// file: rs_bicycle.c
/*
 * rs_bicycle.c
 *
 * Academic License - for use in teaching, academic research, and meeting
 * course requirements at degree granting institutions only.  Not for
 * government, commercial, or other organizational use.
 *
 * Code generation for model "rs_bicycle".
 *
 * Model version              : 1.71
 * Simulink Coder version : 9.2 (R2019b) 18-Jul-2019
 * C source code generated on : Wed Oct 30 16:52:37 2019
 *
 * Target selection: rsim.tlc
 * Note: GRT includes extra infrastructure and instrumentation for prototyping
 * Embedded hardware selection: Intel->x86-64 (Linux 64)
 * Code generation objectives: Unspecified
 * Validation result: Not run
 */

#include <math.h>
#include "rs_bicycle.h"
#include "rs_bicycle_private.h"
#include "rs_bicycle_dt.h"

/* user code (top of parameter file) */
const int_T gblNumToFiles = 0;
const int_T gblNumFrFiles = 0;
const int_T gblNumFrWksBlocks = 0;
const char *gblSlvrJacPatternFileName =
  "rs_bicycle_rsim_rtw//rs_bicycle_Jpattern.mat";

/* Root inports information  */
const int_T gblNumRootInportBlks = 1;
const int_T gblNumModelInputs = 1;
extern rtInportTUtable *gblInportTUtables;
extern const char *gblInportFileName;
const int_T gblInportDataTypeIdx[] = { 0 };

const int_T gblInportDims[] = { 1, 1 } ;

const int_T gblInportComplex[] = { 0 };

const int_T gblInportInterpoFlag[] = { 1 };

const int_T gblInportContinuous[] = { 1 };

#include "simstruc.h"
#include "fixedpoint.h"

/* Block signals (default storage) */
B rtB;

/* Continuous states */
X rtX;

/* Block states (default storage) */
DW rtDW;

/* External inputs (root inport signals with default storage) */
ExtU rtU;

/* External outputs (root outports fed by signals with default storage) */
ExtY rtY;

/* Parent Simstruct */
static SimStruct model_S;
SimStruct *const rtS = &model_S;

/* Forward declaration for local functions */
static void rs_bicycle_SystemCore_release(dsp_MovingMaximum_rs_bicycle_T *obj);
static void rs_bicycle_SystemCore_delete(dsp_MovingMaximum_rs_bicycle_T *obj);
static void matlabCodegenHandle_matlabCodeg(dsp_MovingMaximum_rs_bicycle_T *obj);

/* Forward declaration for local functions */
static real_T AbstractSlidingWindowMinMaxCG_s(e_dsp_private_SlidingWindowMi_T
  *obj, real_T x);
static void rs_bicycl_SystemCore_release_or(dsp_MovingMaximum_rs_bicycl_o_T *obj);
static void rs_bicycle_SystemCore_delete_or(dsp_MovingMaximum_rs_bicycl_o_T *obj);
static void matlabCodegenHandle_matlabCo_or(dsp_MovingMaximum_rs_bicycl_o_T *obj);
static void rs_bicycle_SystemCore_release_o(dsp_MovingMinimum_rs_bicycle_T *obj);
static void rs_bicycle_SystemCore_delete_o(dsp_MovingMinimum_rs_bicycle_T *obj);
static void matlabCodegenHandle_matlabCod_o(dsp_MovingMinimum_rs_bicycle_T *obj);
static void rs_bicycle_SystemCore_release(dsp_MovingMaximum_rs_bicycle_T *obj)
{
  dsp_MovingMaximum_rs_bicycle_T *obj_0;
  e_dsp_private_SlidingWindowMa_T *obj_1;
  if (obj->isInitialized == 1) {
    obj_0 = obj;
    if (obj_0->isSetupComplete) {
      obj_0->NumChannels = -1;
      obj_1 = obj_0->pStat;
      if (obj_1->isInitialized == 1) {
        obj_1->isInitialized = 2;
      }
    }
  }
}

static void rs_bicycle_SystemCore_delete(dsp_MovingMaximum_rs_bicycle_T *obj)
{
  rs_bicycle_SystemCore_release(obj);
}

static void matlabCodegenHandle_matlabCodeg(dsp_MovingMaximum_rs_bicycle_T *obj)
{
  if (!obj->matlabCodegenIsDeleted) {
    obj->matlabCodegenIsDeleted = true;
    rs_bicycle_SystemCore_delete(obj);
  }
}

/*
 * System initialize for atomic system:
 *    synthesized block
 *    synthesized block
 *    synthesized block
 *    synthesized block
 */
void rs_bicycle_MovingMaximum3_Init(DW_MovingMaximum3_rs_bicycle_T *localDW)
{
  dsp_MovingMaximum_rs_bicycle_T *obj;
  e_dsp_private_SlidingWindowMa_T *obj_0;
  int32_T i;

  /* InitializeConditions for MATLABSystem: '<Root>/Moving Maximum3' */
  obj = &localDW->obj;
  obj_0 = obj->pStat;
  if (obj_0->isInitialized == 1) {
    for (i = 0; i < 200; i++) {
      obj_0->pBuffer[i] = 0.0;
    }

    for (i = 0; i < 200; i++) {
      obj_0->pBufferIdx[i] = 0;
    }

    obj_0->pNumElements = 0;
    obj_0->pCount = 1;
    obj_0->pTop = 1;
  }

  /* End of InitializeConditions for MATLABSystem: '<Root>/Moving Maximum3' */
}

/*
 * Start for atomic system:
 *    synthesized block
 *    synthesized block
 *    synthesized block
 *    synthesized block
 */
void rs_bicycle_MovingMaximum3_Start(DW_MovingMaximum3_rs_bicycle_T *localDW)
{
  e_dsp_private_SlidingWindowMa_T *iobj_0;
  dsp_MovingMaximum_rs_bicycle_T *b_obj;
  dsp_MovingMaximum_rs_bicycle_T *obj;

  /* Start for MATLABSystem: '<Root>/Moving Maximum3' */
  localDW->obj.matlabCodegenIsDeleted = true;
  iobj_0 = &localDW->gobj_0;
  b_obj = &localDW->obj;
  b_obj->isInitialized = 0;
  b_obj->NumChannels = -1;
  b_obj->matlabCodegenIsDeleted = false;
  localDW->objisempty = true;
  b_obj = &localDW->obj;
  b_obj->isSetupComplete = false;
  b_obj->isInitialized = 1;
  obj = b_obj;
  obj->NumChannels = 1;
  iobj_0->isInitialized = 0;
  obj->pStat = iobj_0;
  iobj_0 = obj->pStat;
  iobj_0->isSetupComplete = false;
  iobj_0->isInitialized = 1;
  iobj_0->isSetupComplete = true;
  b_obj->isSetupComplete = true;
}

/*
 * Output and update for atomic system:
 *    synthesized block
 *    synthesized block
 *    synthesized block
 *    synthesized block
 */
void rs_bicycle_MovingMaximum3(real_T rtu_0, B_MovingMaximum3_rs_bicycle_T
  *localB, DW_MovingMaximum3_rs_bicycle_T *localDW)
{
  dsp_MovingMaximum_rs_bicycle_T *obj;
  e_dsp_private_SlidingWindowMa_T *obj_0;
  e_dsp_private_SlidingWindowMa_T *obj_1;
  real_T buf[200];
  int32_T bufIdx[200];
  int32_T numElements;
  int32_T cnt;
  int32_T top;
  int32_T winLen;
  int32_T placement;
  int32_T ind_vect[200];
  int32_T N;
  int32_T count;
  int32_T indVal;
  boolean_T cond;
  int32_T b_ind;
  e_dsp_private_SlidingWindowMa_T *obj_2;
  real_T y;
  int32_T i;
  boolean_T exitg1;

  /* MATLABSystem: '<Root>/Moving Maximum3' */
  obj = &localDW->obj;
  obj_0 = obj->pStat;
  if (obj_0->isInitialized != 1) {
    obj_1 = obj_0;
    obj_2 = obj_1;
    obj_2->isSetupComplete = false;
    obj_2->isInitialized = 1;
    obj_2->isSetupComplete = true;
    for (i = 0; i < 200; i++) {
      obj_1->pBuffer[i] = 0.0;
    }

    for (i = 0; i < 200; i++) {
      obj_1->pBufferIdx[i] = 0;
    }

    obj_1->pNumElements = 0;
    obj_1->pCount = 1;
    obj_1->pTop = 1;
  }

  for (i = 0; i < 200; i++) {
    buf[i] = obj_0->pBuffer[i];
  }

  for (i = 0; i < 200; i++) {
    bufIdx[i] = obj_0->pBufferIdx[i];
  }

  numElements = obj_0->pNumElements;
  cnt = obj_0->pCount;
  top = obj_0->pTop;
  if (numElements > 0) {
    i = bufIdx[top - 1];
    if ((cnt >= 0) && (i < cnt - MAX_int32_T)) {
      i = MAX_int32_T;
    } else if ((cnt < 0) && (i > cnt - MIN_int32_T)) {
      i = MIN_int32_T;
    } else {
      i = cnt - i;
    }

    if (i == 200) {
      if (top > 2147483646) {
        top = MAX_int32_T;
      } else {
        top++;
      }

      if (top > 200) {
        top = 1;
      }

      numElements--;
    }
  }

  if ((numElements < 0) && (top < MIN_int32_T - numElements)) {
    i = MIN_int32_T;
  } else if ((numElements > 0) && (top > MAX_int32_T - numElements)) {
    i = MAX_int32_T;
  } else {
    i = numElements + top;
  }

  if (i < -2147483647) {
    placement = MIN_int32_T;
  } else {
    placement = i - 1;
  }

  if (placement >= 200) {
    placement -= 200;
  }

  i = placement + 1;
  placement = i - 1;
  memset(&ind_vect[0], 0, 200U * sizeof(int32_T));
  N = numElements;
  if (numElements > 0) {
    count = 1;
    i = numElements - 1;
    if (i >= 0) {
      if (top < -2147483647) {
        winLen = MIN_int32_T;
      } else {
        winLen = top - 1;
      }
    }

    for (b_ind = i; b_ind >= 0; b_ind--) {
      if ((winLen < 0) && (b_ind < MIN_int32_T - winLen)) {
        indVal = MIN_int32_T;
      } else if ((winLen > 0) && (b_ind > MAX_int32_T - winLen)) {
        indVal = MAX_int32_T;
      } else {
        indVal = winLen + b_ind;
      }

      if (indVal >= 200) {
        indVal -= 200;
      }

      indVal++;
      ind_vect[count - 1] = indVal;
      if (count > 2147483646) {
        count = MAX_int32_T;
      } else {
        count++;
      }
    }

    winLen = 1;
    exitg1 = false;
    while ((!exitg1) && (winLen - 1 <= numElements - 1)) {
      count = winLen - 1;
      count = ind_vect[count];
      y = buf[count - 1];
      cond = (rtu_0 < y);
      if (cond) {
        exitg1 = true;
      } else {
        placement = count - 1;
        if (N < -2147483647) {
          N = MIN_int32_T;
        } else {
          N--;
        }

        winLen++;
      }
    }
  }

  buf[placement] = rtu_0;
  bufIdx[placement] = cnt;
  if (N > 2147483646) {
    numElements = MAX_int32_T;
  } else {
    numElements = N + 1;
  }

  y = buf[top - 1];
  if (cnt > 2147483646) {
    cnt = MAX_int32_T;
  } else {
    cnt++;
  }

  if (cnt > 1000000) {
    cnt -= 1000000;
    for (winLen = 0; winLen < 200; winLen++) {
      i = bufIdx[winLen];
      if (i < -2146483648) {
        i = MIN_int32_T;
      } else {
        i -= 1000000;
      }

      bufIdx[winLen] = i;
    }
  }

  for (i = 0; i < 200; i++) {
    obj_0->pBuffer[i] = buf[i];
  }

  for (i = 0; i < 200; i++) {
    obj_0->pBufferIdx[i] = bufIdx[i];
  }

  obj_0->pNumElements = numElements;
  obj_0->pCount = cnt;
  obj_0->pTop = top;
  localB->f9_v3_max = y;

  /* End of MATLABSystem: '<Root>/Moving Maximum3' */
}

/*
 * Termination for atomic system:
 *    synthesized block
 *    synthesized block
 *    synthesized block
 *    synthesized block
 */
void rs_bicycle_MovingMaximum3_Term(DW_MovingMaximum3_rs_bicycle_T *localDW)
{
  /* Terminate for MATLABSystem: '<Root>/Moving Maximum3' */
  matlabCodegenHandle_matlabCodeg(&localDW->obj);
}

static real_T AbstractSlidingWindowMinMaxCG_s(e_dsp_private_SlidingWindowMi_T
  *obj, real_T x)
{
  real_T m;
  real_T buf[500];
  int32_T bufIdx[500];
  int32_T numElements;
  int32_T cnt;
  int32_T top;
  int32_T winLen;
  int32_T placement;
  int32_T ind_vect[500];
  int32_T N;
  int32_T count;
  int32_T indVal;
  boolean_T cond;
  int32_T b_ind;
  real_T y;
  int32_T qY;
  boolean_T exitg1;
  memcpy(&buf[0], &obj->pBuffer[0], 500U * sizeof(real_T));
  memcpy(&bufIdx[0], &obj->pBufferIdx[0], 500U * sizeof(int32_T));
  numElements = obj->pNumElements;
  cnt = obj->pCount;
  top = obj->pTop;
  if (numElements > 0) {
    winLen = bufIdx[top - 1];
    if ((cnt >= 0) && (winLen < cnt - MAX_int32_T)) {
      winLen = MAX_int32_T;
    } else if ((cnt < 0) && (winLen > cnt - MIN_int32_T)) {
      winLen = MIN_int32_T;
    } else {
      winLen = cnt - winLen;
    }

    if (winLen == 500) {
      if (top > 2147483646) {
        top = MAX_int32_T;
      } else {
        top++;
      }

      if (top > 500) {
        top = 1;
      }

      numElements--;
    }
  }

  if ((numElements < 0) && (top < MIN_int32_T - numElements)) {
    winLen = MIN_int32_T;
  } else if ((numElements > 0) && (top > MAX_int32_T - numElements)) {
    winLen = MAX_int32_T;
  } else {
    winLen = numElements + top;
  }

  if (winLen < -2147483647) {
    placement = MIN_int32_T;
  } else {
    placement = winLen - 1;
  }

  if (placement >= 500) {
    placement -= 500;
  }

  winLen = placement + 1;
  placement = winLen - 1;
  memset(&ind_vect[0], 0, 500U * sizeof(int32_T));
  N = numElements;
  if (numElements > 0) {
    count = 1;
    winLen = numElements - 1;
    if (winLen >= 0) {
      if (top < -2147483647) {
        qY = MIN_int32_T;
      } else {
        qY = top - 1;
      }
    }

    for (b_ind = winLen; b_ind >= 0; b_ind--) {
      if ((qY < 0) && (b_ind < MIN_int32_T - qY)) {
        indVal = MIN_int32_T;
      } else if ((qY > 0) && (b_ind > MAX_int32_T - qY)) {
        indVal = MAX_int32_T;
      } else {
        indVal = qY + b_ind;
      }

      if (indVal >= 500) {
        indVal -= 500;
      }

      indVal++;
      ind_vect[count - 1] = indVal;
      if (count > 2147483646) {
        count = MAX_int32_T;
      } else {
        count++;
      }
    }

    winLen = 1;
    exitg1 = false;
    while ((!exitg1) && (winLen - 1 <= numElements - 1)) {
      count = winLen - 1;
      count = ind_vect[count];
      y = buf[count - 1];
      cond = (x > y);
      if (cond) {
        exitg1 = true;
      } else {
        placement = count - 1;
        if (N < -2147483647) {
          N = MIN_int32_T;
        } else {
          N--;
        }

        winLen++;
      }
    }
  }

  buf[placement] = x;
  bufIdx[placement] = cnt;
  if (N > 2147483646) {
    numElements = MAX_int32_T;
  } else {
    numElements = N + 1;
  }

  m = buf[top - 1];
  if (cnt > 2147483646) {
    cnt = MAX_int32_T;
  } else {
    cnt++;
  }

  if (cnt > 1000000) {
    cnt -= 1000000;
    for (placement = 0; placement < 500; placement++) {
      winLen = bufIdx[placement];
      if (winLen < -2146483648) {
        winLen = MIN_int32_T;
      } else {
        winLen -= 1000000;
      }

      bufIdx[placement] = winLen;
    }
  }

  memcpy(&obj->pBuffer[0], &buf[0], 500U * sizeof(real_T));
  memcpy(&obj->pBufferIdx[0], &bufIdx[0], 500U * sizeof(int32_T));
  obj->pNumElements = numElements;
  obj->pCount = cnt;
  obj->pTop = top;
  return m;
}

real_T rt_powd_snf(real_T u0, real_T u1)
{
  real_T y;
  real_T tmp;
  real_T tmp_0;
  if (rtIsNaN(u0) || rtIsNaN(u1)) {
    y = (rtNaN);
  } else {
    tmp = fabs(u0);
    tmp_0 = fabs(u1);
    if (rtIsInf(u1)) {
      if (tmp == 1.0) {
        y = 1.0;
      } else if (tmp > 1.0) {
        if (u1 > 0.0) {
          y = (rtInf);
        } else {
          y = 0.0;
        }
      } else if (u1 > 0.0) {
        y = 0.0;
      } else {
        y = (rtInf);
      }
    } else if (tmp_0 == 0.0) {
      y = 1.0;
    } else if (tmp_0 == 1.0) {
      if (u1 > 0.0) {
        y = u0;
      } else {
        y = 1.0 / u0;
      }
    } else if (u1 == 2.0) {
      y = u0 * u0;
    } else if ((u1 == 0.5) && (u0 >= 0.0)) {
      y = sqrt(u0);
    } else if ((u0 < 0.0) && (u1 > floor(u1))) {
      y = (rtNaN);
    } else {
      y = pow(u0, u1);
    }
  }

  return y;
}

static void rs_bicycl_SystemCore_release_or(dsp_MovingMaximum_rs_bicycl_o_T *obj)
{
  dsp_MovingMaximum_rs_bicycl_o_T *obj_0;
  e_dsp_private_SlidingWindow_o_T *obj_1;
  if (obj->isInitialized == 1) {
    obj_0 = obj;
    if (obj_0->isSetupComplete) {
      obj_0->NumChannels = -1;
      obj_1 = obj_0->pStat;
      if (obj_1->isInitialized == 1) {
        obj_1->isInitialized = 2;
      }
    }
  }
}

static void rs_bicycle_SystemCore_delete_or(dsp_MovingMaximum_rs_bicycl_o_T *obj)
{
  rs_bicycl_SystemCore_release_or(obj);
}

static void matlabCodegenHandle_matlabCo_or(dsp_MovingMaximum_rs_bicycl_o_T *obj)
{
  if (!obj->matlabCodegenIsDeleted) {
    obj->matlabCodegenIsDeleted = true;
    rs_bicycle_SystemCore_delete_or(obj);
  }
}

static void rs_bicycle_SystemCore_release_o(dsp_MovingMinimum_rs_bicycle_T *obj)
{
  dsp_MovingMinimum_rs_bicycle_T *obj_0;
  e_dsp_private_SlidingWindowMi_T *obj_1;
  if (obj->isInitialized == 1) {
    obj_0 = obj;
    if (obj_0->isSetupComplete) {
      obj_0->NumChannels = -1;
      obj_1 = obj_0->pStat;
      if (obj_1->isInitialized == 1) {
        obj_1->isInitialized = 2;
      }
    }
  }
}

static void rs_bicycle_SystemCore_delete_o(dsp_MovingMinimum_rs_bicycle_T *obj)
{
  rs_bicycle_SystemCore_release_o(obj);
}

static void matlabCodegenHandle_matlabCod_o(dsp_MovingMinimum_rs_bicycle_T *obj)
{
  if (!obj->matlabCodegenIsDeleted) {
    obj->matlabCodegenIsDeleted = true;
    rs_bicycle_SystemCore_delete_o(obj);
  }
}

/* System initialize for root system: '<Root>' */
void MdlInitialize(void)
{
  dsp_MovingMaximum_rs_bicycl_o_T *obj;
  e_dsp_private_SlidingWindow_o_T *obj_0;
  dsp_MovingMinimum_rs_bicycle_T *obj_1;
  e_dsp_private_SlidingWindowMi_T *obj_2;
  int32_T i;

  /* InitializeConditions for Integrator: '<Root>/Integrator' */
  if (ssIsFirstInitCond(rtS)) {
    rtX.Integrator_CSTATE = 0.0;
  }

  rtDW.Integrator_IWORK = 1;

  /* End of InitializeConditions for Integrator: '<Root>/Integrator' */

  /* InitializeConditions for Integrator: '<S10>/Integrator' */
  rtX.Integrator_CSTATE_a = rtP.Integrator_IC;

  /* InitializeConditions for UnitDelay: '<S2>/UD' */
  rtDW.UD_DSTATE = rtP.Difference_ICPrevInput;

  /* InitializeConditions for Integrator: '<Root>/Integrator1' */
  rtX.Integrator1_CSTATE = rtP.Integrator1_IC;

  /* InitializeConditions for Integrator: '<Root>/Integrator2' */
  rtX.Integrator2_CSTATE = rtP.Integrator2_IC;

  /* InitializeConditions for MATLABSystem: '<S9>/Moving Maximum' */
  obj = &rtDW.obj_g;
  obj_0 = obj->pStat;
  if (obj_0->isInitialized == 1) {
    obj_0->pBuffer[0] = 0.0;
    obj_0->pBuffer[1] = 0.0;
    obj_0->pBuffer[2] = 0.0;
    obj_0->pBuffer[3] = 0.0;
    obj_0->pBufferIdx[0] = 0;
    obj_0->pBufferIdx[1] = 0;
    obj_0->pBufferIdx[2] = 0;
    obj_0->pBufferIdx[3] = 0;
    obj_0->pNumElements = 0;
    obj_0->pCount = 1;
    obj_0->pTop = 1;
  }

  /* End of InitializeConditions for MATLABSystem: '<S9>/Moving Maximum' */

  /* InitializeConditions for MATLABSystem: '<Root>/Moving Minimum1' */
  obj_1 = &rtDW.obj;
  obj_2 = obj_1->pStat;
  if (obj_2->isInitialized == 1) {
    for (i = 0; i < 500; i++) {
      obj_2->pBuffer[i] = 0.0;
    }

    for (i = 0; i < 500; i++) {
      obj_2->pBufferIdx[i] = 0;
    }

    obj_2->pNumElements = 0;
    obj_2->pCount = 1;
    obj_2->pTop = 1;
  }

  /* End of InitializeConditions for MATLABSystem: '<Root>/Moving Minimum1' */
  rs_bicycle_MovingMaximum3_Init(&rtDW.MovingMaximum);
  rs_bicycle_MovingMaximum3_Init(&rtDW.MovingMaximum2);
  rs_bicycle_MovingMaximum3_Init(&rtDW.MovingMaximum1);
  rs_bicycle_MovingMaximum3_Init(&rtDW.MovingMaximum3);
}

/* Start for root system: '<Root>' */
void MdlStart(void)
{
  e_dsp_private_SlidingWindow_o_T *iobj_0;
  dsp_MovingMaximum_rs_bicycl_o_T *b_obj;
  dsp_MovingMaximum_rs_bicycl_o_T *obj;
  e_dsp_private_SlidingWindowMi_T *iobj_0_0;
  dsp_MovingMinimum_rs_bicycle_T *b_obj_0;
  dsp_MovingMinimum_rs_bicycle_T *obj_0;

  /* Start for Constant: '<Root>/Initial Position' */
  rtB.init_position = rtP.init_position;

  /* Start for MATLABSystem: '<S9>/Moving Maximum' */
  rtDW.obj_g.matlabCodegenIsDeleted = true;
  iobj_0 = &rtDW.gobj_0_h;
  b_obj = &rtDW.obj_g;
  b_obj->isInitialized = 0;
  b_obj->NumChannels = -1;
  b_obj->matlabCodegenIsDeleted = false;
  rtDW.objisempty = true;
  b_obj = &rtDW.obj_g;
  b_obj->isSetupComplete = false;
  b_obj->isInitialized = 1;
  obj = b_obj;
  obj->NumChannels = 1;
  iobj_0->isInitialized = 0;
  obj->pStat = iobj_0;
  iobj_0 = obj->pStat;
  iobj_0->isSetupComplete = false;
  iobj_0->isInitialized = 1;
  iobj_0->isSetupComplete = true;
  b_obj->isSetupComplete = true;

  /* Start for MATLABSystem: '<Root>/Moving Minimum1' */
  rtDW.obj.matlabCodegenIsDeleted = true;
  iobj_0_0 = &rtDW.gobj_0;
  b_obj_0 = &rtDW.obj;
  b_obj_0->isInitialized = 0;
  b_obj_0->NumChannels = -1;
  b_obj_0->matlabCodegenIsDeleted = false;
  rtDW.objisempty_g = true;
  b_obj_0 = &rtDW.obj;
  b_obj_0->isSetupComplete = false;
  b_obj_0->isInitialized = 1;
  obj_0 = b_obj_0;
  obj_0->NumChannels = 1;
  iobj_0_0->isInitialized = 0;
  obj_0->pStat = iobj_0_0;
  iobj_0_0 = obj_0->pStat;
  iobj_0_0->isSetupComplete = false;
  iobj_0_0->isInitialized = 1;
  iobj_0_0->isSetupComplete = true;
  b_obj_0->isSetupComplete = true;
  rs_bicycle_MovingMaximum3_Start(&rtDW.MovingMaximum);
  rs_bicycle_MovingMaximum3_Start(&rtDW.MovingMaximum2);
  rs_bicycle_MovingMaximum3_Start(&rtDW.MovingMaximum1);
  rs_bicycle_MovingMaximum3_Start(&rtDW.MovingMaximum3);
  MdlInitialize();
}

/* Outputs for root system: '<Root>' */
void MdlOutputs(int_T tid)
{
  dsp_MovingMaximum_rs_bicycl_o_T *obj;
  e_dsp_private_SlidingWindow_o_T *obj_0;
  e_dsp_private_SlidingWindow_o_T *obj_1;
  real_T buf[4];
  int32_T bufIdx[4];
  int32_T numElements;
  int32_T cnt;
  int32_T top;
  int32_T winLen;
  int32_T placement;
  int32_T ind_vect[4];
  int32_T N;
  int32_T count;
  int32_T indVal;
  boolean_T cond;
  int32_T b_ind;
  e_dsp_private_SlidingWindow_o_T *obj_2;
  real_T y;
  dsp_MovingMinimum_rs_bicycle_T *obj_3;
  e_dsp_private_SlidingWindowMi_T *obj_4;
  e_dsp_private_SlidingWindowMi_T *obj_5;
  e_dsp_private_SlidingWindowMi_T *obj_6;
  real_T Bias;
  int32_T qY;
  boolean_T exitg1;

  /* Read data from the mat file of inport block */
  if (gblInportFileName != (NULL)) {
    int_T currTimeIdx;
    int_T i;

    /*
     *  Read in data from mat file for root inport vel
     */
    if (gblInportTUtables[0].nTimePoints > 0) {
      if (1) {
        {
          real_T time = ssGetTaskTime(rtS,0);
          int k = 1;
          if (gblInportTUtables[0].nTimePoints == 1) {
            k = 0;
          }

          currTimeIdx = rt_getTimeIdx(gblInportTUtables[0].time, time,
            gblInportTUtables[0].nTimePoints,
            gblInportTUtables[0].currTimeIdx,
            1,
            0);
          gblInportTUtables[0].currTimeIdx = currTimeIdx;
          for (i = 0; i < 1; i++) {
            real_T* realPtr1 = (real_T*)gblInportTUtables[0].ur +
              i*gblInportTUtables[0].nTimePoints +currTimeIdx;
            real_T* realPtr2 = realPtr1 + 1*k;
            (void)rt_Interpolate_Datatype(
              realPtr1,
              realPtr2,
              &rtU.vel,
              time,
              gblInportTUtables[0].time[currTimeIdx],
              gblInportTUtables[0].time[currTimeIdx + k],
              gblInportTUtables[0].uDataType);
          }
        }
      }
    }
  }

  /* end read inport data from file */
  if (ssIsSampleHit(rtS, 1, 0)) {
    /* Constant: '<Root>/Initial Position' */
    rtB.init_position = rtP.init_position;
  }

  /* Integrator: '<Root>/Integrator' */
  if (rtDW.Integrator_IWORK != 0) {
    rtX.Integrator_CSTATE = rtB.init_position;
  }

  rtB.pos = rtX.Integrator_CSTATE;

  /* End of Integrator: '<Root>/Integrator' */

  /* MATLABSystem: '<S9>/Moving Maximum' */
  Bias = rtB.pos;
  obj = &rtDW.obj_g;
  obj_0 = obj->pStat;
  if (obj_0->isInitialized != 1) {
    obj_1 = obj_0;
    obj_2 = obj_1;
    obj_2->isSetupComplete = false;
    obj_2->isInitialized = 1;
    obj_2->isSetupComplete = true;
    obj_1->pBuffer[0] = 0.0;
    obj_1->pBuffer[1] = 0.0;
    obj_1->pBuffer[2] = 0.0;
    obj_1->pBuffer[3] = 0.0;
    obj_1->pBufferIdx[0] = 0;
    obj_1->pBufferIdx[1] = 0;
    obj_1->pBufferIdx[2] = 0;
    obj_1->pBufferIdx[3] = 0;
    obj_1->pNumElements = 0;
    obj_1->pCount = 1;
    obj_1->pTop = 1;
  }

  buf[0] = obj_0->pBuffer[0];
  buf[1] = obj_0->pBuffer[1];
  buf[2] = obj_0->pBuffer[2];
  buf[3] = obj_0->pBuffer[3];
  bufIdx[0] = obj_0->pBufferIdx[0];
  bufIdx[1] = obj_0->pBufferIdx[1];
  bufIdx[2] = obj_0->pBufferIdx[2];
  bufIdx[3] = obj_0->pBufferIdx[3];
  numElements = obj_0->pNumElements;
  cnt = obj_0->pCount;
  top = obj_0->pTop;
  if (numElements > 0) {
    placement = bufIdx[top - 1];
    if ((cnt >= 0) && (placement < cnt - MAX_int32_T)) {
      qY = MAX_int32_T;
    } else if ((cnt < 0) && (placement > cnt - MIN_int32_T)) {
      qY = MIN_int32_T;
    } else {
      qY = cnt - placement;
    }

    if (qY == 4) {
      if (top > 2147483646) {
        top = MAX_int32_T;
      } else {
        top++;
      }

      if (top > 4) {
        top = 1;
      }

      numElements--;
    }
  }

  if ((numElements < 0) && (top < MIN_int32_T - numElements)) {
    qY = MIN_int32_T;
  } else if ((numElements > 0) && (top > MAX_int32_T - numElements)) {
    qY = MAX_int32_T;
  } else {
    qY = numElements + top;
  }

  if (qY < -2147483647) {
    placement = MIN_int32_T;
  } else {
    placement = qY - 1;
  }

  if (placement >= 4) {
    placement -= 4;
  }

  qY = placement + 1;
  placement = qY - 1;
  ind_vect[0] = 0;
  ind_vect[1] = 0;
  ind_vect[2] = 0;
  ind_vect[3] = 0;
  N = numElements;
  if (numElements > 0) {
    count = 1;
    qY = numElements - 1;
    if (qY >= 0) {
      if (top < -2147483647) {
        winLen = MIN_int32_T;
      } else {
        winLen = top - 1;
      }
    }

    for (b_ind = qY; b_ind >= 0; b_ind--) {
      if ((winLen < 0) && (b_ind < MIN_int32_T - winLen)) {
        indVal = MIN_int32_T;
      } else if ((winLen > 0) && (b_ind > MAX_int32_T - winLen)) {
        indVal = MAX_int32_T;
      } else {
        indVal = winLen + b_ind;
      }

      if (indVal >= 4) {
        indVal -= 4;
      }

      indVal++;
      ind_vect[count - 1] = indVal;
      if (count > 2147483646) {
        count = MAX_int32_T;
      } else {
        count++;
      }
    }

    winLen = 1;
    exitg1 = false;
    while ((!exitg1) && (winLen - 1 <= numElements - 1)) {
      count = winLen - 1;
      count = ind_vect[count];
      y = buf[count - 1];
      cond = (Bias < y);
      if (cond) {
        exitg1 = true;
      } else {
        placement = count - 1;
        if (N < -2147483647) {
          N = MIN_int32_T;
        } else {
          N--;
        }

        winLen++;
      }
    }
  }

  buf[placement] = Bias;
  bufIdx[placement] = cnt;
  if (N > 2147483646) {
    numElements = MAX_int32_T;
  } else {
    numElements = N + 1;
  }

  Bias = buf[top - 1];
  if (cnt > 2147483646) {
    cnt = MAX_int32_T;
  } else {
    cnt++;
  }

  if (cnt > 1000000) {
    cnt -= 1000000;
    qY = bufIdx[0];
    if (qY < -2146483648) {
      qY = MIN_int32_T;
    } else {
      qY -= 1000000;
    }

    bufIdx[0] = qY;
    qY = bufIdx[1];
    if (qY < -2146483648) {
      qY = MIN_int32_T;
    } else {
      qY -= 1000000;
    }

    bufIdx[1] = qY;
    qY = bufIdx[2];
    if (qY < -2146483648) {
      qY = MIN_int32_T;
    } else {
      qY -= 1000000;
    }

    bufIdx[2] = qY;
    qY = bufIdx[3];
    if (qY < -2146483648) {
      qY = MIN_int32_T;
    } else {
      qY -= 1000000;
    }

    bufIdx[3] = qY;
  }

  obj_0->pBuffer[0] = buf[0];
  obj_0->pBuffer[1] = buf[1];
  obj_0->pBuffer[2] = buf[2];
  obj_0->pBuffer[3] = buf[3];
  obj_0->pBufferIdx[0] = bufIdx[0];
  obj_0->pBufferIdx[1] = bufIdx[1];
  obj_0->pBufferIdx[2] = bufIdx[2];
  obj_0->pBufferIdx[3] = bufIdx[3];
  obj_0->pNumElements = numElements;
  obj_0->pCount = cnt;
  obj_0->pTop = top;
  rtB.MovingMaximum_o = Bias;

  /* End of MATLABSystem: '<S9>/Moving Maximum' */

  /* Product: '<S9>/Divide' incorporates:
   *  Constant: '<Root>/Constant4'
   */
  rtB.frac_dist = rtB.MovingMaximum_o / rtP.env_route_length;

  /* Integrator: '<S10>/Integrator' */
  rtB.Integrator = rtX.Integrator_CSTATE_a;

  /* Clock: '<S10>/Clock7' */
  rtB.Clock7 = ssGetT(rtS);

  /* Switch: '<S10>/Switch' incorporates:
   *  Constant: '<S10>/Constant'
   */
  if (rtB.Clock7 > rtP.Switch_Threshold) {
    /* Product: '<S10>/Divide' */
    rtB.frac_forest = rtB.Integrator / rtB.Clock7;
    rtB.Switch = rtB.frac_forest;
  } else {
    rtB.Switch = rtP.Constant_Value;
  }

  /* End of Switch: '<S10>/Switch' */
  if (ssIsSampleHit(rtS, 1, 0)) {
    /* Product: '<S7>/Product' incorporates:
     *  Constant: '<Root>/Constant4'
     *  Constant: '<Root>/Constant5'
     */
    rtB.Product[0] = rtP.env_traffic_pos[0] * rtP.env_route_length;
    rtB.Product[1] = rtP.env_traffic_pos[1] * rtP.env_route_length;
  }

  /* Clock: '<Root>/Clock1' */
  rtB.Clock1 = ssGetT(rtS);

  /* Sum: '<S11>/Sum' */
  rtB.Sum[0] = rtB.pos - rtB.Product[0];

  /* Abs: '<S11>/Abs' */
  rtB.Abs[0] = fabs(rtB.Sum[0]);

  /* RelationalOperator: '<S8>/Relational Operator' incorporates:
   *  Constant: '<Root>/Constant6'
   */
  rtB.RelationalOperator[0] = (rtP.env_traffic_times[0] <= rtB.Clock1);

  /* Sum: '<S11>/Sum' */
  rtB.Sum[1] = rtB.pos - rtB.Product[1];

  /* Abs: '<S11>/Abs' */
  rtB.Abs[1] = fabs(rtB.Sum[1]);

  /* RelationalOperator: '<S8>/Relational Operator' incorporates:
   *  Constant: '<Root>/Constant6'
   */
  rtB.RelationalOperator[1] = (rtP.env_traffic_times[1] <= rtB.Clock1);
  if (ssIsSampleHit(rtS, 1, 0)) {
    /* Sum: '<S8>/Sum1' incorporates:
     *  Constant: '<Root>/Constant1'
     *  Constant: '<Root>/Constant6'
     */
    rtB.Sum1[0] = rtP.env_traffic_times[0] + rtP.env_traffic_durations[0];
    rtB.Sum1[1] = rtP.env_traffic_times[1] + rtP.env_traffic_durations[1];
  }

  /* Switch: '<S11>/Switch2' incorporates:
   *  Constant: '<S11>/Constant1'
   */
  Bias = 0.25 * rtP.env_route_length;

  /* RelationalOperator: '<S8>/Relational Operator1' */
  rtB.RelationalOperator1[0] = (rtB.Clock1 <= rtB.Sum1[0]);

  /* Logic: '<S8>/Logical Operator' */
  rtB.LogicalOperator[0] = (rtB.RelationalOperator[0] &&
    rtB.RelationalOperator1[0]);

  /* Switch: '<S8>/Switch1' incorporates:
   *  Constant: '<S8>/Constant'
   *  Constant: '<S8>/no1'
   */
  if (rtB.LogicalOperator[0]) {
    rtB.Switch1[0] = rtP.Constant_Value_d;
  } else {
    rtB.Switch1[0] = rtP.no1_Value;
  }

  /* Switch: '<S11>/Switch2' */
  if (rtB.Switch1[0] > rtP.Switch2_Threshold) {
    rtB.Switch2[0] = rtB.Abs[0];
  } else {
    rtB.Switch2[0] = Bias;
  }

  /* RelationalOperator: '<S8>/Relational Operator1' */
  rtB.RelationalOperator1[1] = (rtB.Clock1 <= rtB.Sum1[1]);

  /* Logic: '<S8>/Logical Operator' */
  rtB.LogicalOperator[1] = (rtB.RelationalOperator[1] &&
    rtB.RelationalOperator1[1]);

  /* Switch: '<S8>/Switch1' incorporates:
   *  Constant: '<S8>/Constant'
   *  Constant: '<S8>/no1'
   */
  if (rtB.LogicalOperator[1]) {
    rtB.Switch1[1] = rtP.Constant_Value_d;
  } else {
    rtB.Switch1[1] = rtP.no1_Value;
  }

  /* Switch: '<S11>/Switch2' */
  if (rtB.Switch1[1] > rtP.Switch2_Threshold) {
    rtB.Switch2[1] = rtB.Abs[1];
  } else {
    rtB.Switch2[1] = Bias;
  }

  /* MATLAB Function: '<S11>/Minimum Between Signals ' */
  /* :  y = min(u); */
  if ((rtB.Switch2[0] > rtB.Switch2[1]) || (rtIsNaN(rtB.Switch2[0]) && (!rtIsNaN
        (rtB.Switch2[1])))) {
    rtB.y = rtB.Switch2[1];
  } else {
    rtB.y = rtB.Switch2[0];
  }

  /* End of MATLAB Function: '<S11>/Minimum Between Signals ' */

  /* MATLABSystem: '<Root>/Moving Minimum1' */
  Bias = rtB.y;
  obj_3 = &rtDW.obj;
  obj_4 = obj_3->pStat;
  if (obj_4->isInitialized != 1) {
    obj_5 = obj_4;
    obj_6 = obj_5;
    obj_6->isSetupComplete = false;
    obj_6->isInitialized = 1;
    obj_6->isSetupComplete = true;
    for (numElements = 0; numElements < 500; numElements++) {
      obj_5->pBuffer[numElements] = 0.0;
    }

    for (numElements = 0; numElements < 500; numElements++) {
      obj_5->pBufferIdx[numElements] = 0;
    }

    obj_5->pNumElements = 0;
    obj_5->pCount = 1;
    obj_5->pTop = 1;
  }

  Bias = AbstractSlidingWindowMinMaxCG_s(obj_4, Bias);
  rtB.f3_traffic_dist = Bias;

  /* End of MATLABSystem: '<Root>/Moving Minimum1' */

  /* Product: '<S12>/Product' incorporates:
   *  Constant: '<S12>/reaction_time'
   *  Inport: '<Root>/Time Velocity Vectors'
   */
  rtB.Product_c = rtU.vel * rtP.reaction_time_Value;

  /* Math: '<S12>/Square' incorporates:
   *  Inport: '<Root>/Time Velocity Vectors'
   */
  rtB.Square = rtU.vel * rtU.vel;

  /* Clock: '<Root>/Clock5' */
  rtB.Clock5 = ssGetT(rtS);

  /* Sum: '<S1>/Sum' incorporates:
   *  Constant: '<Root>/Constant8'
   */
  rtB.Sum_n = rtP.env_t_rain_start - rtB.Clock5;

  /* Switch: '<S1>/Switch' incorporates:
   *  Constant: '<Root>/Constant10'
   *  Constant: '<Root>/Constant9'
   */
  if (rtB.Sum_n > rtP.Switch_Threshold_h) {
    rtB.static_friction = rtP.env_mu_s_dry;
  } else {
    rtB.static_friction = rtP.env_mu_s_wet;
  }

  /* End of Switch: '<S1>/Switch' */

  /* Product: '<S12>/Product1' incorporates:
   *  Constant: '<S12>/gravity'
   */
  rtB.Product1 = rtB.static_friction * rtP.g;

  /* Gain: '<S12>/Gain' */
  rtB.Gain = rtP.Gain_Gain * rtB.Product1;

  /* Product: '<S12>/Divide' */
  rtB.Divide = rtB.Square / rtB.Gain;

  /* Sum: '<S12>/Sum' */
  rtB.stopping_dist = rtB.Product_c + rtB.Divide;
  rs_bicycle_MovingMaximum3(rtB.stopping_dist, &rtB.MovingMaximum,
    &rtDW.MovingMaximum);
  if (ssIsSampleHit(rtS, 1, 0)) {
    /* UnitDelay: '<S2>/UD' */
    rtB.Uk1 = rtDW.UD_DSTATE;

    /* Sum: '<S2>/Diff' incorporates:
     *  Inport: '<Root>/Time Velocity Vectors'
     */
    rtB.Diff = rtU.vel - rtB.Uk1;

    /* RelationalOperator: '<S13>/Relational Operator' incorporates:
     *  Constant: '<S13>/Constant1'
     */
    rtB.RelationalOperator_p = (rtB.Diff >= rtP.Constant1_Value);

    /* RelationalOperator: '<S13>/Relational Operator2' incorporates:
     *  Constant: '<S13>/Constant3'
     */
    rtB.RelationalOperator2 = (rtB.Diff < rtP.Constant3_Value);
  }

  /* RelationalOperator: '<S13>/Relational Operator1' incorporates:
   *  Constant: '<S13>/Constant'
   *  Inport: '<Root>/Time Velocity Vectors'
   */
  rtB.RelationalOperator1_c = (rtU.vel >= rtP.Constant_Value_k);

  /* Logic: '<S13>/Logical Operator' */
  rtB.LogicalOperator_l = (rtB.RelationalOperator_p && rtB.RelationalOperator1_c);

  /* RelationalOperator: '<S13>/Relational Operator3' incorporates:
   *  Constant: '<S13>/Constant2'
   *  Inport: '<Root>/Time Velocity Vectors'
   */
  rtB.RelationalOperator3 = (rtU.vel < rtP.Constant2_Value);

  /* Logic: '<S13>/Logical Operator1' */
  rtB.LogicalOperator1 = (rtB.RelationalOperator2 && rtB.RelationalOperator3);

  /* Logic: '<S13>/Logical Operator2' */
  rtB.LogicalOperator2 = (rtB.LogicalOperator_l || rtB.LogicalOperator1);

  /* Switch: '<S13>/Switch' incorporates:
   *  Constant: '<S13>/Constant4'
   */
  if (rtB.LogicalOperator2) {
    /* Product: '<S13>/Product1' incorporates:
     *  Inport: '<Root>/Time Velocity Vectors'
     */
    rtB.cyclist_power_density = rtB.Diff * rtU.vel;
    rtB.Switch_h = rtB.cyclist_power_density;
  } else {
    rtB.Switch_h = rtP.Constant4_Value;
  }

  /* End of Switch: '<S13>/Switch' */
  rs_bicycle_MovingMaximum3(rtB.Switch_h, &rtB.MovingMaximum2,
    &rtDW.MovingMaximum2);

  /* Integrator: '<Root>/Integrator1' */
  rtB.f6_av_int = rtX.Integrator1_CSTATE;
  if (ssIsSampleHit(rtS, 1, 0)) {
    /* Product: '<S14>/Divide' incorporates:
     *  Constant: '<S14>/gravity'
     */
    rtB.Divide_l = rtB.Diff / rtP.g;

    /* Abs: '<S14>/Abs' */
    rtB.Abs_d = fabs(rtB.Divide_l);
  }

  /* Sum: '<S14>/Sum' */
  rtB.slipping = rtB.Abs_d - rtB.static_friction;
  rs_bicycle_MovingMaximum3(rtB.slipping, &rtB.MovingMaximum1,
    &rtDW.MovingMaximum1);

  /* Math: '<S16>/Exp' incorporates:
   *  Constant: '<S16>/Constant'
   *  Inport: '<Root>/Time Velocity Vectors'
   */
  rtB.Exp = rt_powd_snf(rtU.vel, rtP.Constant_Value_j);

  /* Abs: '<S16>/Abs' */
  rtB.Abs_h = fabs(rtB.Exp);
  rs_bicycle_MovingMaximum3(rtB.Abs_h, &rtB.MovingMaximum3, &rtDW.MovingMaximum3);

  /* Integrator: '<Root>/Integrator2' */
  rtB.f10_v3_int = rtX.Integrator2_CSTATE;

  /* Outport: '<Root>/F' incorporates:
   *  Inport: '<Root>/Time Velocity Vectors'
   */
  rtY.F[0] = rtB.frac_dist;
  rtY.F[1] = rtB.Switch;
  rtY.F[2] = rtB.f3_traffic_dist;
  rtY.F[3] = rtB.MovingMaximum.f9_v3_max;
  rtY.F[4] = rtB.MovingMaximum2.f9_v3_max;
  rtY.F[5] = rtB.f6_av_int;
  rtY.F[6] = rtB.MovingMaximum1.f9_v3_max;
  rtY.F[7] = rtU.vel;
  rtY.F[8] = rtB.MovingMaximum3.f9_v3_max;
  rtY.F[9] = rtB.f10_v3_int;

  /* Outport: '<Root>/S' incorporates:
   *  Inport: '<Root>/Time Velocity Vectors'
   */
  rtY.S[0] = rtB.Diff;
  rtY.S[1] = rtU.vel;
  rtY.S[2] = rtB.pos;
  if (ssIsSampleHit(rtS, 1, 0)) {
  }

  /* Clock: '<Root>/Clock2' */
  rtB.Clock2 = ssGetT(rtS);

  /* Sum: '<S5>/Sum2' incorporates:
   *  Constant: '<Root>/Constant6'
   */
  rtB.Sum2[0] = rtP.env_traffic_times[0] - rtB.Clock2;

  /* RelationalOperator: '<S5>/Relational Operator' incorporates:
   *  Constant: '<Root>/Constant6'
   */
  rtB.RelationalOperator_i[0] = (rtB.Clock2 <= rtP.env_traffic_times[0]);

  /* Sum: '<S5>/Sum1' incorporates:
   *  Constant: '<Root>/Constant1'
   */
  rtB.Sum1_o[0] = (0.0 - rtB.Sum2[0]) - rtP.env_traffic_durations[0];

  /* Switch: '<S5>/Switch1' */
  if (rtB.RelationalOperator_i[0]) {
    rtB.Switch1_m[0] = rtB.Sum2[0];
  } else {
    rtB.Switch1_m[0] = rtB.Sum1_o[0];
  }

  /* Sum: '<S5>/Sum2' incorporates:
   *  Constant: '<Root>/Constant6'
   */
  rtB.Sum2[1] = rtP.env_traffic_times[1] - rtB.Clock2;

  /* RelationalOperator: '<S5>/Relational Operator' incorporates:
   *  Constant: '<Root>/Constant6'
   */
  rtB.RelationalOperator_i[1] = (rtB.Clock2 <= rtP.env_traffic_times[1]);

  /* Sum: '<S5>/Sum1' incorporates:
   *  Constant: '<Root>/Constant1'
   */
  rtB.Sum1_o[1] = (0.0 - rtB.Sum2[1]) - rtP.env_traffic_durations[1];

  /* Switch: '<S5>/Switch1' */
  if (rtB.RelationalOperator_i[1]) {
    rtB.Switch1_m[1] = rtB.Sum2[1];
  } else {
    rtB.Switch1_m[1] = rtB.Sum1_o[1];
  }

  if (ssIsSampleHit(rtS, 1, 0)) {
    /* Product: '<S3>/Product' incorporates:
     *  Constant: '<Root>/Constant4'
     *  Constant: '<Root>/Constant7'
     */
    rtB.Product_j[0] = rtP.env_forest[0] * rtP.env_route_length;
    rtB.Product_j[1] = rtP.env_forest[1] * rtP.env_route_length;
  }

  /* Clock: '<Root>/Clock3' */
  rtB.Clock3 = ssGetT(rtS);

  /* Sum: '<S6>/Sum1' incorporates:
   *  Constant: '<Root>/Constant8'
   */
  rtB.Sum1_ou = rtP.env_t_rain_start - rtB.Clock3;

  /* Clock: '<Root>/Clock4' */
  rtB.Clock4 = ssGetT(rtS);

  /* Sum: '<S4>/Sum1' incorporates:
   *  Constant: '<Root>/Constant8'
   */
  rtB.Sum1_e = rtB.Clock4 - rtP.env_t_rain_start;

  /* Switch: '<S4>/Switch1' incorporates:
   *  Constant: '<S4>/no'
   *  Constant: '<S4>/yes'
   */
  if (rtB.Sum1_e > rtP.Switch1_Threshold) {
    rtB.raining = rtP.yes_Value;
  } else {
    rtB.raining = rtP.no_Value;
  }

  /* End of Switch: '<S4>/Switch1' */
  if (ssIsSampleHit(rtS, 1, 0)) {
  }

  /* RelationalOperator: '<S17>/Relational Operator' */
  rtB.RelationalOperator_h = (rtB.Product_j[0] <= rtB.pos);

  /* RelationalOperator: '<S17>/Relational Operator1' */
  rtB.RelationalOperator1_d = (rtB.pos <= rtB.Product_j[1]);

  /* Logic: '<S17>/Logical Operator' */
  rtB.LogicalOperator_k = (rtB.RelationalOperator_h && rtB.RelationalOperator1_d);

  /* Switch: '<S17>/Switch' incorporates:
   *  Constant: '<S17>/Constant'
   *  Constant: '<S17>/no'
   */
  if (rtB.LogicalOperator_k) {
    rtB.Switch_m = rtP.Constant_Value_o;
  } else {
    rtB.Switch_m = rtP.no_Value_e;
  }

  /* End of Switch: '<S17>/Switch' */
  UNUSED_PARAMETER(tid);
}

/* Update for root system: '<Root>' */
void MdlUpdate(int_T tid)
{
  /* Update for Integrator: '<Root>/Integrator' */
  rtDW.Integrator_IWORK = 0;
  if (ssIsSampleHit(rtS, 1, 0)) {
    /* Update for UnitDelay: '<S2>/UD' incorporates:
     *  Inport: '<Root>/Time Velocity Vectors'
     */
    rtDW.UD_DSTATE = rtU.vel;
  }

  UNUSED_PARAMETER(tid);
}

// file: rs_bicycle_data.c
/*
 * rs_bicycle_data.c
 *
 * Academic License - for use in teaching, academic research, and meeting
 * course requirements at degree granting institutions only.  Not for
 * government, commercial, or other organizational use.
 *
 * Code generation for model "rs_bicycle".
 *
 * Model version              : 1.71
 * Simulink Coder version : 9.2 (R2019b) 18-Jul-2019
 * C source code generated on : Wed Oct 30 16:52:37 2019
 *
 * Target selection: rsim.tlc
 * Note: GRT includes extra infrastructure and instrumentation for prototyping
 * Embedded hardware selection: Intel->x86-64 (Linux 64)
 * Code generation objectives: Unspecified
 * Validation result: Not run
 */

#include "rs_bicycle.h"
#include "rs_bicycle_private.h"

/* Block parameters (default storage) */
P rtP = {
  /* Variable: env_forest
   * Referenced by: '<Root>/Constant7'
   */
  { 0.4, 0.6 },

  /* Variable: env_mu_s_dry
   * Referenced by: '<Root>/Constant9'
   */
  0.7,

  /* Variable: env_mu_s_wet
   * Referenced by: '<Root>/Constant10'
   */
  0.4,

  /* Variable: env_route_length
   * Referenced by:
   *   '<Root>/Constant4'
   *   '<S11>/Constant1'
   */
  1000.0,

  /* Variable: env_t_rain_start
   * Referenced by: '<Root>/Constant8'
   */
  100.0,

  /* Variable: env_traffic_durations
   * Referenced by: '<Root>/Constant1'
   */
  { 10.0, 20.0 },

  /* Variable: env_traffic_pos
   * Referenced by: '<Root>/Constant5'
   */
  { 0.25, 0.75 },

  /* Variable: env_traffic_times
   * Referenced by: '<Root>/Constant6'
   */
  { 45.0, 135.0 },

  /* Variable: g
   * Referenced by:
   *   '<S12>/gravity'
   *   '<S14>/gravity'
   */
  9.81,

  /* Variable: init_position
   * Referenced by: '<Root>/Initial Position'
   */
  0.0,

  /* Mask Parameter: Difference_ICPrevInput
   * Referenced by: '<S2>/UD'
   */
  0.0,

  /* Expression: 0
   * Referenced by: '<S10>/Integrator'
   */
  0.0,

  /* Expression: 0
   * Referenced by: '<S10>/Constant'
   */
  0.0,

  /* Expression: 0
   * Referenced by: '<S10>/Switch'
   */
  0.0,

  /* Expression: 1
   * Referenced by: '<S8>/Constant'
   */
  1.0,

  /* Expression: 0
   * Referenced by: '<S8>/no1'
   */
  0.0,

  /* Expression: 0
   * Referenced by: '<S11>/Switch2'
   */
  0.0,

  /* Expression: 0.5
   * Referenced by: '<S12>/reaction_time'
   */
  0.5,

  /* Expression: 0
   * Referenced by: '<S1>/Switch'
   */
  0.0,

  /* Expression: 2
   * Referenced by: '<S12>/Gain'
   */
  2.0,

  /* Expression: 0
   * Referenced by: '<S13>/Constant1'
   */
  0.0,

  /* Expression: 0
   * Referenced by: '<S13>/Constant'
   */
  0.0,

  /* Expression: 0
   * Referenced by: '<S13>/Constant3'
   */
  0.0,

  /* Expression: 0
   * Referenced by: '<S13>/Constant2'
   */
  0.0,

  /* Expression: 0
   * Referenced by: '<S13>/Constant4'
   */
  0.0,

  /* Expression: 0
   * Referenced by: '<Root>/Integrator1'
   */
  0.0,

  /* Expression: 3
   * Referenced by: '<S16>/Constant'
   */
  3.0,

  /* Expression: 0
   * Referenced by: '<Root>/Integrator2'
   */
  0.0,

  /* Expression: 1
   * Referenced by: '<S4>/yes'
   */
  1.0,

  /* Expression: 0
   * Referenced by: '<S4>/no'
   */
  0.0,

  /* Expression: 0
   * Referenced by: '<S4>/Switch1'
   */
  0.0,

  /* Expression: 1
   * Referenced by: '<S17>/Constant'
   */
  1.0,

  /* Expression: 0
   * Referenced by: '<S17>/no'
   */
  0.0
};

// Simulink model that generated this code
simulink model "rs_bicycle"  (R2019b)
settings: Solver=FixedStepAuto  StartTime=0.0  StopTime=200  FixedStep=4  RelTol=1e-3
undefined symbols (not defined in the file): duration, env_forest, env_mu_s_dry, env_mu_s_wet, env_route_length, env_t_rain_start, env_traffic_durations, env_traffic_pos, env_traffic_times, g, init_position
libraries: dspstat3 x6, simulink x1

== system rs_bicycle ==
  note: Guidance Solution for
      | Dynamics $\mathcal{S}(t)$
  note: Fixed Decision
      | Components $(s)$
  note: Environment Parameters $\mathcal{P}(t)$
  note: 'From Velocity'
      | Constructor $\mathcal{C}(x,p)$
  note: Transient Parameter Limit $\mathcal{P}(t)$
  Time Velocity Vectors : Inport
  Auxilliary Scope : Scope  NumInputPorts=6
  Bus Creator : BusCreator  Inputs=2
  Bus Creator1 : BusCreator  Inputs=9
  Bus Creator2 : BusCreator  Inputs=3
  Bus Creator3 : BusCreator  Inputs=4
  Bus Creator4 : BusCreator  Inputs=7
  Bus Creator5 : BusCreator  Inputs=10
  Clock{1..5} (5 alike) : Clock
  Constant1 : Constant  Value=env_traffic_durations
  Constant10 : Constant  Value=env_mu_s_wet
  Constant4 : Constant  Value=env_route_length
  Constant5 : Constant  Value=env_traffic_pos
  Constant6 : Constant  Value=env_traffic_times
  Constant7 : Constant  Value=env_forest
  Constant8 : Constant  Value=env_t_rain_start
  Constant9 : Constant  Value=env_mu_s_dry
  Current Static Friction : Subsystem
  Difference : simulink/Discrete/Difference  ICPrevInput=0.0  OutMin=[]  OutMax=[]  OutDataType=fixdt(1, 16)  OutScaling=2^-10  RndMeth=Round  DoSatur=off
  Duration : Constant  Value=duration
  Forest Boundaries : Subsystem
  Initial Position : Constant  Value=init_position
  Integrator : Integrator  InitialConditionSource=external  InitialCondition=init_position
  Integrator1 : Integrator
  Integrator2 : Integrator
  Moving Maximum{,1..3} (4 alike) : dspstat3/Moving Maximum  SpecifyWindowLength=on  WindowLength=duration  SimulateUsing=Code generation
  Moving Minimum1 : dspstat3/Moving Minimum  SpecifyWindowLength=on  WindowLength=500  SimulateUsing=Code generation
  Performance Metric Scope : Scope  NumInputPorts=10
  Raining Boolean : Subsystem
  Scope2 : Scope  NumInputPorts=7
  Solution Scope : Scope  NumInputPorts=3
  Time From Traffic Encounter : Subsystem
  Time Until Raining : Subsystem
  To Workspace : ToWorkspace  VariableName=WS_S  SaveFormat=Timeseries  SampleTime=-1
  To Workspace1 : ToWorkspace  VariableName=WS_s  SaveFormat=Timeseries  SampleTime=-1
  To Workspace2 : ToWorkspace  VariableName=WS_P  SaveFormat=Timeseries  SampleTime=-1
  To Workspace3 : ToWorkspace  VariableName=WS_p  SaveFormat=Timeseries  SampleTime=-1
  To Workspace4 : ToWorkspace  VariableName=wf  SaveFormat=Timeseries  SampleTime=-1
  Traffic Location(s) : Subsystem
  Traffic Passing : Subsystem
  aux1: Fraction of Route Distance : Subsystem
  aux2: Fraction Spent In Forest : Subsystem
  aux3: Closest Instantaenous Traffic : Subsystem
  aux4: Instantaneous Stopping Distance : Subsystem
  aux5: Cyclist Power Density Transfer : Subsystem
  aux6: Exceedance of Static Friction (slipping) : Subsystem
  aux7: Final Velocity : Subsystem
  aux8: Drag Power Compensation (V^3) : Subsystem
  F : Outport  PortDimensions=10
  S : Outport  Port=2  PortDimensions=3
  wires:
  Initial Position/1 -> Integrator/2, Bus Creator/1  "init_position"
  Constant4/1 -> Bus Creator1/2  "env_route_length"
  Constant5/1 -> Bus Creator1/3  "env_traffic_pos"
  Constant6/1 -> Bus Creator1/4  "env_traffic_times"
  Constant7/1 -> Bus Creator1/6  "env_forest"
  Constant9/1 -> Bus Creator1/8  "env_mu_s_dry"
  Constant8/1 -> Bus Creator1/7  "env_t_rain_start"
  Constant10/1 -> Bus Creator1/9  "env_mu_s_wet"
  Bus Creator1/1 -> Current Static Friction/1(env), Raining Boolean/1(env), Time Until Raining/1(env), Traffic Location(s)/1(env), Time From Traffic Encounter/1(env), Traffic Passing/1(env), Forest Boundaries/1(env), To Workspace3/1, Bus Creator3/3  "p"
  Duration/1 -> Bus Creator1/1, Bus Creator/2  "duration"
  Clock1/1 -> Traffic Passing/2(t)
  Clock2/1 -> Time From Traffic Encounter/2(t1)
  Clock3/1 -> Time Until Raining/2(t)
  Clock4/1 -> Raining Boolean/2(t)
  Clock5/1 -> Current Static Friction/2(t)
  Time From Traffic Encounter/1(time_from_traffic) -> Scope2/1, Bus Creator4/1  "time_from_traffic"
  Traffic Passing/1(passing) -> Scope2/2, Bus Creator4/2  "traffic_passing"
  Forest Boundaries/1(forest_bounds) -> Scope2/3, Bus Creator4/3  "forest_bounds"
  Traffic Location(s)/1(traffic_pos) -> Scope2/4, Bus Creator4/4  "traffic_pos"
  Time Until Raining/1(until_raining) -> Scope2/5, Bus Creator4/5  "until_raining"
  Raining Boolean/1(raining) -> Scope2/6, Bus Creator4/6  "raining"
  Current Static Friction/1(static_friction) -> Scope2/7, Bus Creator4/7  "static_friction"
  Bus Creator4/1 -> To Workspace2/1, Bus Creator3/4  "P"
  Bus Creator2/1 -> S/1, Bus Creator3/1, To Workspace/1  "S"
  Bus Creator3/1 -> aux3: Closest Instantaenous Traffic/1(In1), aux1: Fraction of Route Distance/1(In1), aux2: Fraction Spent In Forest/1(In1), aux8: Drag Power Compensation (V^3)/1(In1), aux7: Final Velocity/1(In1), aux6: Exceedance of Static Friction (slipping)/1(In1), aux5: Cyclist Power Density Transfer/1(In1), aux4: Instantaneous Stopping Distance/1(In1)
  Constant1/1 -> Bus Creator1/5  "env_traffic_durations"
  aux1: Fraction of Route Distance/1(aux1) -> Performance Metric Scope/1, Bus Creator5/1, Auxilliary Scope/1  "f1_frac_route"
  aux2: Fraction Spent In Forest/1(aux2) -> Performance Metric Scope/2, Bus Creator5/2, Auxilliary Scope/2  "f2_frac_forest"
  aux3: Closest Instantaenous Traffic/1(aux1) -> Auxilliary Scope/3, Moving Minimum1/1  "aux3: traffic"
  aux4: Instantaneous Stopping Distance/1(aux4) -> Moving Maximum/1, Auxilliary Scope/4  "aux4: stopping_dist"
  aux5: Cyclist Power Density Transfer/1(aux5) -> Integrator1/1, Moving Maximum2/1, Auxilliary Scope/5  "aux5: power_density"
  aux6: Exceedance of Static Friction (slipping)/1(aux6) -> Moving Maximum1/1, Auxilliary Scope/6  "aux6: slipping"
  Moving Maximum1/1 -> Performance Metric Scope/7, Bus Creator5/7  "f7_slip_max"
  Moving Maximum/1 -> Performance Metric Scope/4, Bus Creator5/4  "f4_stop_dist"
  Moving Maximum2/1 -> Performance Metric Scope/5, Bus Creator5/5  "f5_av_max"
  Bus Creator5/1 -> To Workspace4/1, F/1
  Difference/1 -> Bus Creator2/1, Solution Scope/1  "acc"
  Integrator/1 -> Bus Creator2/3, Solution Scope/3  "pos"
  Bus Creator/1 -> To Workspace1/1, Bus Creator3/2
  Time Velocity Vectors/1 -> Difference/1, Integrator/1, Bus Creator2/2, Solution Scope/2  "vel"
  Moving Minimum1/1 -> Performance Metric Scope/3, Bus Creator5/3  "f3_traffic_dist"
  aux7: Final Velocity/1(aux7) -> Bus Creator5/8, Performance Metric Scope/8  "f8_v_final"
  aux8: Drag Power Compensation (V^3)/1(aux8) -> Integrator2/1, Moving Maximum3/1  "aux8: v3"
  Moving Maximum3/1 -> Performance Metric Scope/9, Bus Creator5/9  "f9_v3_max"
  Integrator2/1 -> Performance Metric Scope/10, Bus Creator5/10  "f10_v3_int"
  Integrator1/1 -> Performance Metric Scope/6, Bus Creator5/6  "f6_av_int"

== system rs_bicycle/Current Static Friction ==
  env : Inport
  t : Inport  Port=2
  Bus Selector : BusSelector  OutputSignals=env_mu_s_dry,env_t_rain_start,env_mu_s_wet
  Sum : Sum  Inputs=|+-
  Switch : Switch  Criteria=u2 > Threshold
  static_friction : Outport
  wires:
  Bus Selector/2 -> Sum/1  "<env_t_rain_start>"
  t/1 -> Sum/2
  Bus Selector/1 -> Switch/1  "<env_mu_s_dry>"
  Sum/1 -> Switch/2
  env/1 -> Bus Selector/1
  Bus Selector/3 -> Switch/3  "<env_mu_s_wet>"
  Switch/1 -> static_friction/1  "static_friction"

== system rs_bicycle/Forest Boundaries ==
  env : Inport
  Bus Selector : BusSelector  OutputSignals=env_forest,env_route_length
  Product : Product
  forest_bounds : Outport
  wires:
  Bus Selector/1 -> Product/1  "<env_forest>"
  Bus Selector/2 -> Product/2  "<env_route_length>"
  Product/1 -> forest_bounds/1
  env/1 -> Bus Selector/1

== system rs_bicycle/Raining Boolean ==
  env : Inport
  t : Inport  Port=2
  Bus Selector1 : BusSelector  OutputSignals=env_t_rain_start
  Sum1 : Sum  Inputs=|-+
  Switch1 : Switch  Criteria=u2 > Threshold
  no : Constant  Value=0
  yes : Constant
  raining : Outport
  wires:
  yes/1 -> Switch1/1
  Bus Selector1/1 -> Sum1/1  "<env_t_rain_start>"
  no/1 -> Switch1/3
  Switch1/1 -> raining/1  "raining"
  env/1 -> Bus Selector1/1
  Sum1/1 -> Switch1/2
  t/1 -> Sum1/2

== system rs_bicycle/Time From Traffic Encounter ==
  env : Inport
  t1 : Inport  Port=2
  Bus Selector1 : BusSelector  OutputSignals=env_traffic_times,env_traffic_durations
  Relational Operator : RelationalOperator  Operator=<=  OutDataTypeStr=boolean  RndMeth=Simplest
  Sum1 : Sum  Inputs=--|
  Sum2 : Sum  Inputs=|+-
  Switch1 : Switch  Criteria=u2 > Threshold
  time_from_traffic : Outport
  wires:
  Bus Selector1/2 -> Sum1/2  "<env_traffic_durations>"
  Bus Selector1/1 -> Relational Operator/2, Sum2/1  "<env_traffic_times>"
  Switch1/1 -> time_from_traffic/1
  env/1 -> Bus Selector1/1
  Sum1/1 -> Switch1/3
  Sum2/1 -> Sum1/1, Switch1/1
  Relational Operator/1 -> Switch1/2
  t1/1 -> Relational Operator/1, Sum2/2

== system rs_bicycle/Time Until Raining ==
  env : Inport
  t : Inport  Port=2
  Bus Selector1 : BusSelector  OutputSignals=env_t_rain_start
  Sum1 : Sum  Inputs=|+-
  until_raining : Outport
  wires:
  Bus Selector1/1 -> Sum1/1  "<env_t_rain_start>"
  env/1 -> Bus Selector1/1
  t/1 -> Sum1/2
  Sum1/1 -> until_raining/1

== system rs_bicycle/Traffic Location(s) ==
  env : Inport
  Bus Selector : BusSelector  OutputSignals=env_traffic_pos,env_route_length
  Product : Product
  traffic_pos : Outport
  wires:
  Bus Selector/1 -> Product/1  "<env_traffic_pos>"
  Bus Selector/2 -> Product/2  "<env_route_length>"
  Product/1 -> traffic_pos/1
  env/1 -> Bus Selector/1

== system rs_bicycle/Traffic Passing ==
  env : Inport
  t : Inport  Port=2
  Bus Selector : BusSelector  OutputSignals=env_traffic_times,env_traffic_durations
  Constant : Constant
  Logical Operator : Logic  AllPortsSameDT=off  OutDataTypeStr=boolean
  Relational Operator : RelationalOperator  Operator=<=  OutDataTypeStr=boolean  RndMeth=Simplest
  Relational Operator1 : RelationalOperator  Operator=<=  OutDataTypeStr=boolean  RndMeth=Simplest
  Sum1 : Sum  Inputs=++|
  Switch1 : Switch  Criteria=u2 > Threshold
  no1 : Constant  Value=0
  passing : Outport
  wires:
  env/1 -> Bus Selector/1
  Logical Operator/1 -> Switch1/2
  Relational Operator1/1 -> Logical Operator/2
  t/1 -> Relational Operator/2, Relational Operator1/1
  no1/1 -> Switch1/3
  Relational Operator/1 -> Logical Operator/1
  Switch1/1 -> passing/1
  Constant/1 -> Switch1/1
  Sum1/1 -> Relational Operator1/2
  Bus Selector/1 -> Sum1/1, Relational Operator/1  "<env_traffic_times>"
  Bus Selector/2 -> Sum1/2  "<env_traffic_durations>"

== system rs_bicycle/aux1: Fraction of Route Distance ==
  In1 : Inport
  Bus Selector : BusSelector  OutputSignals=S.pos,p.env_route_length
  Divide : Product  Inputs=*/
  Moving Maximum : dspstat3/Moving Maximum  SpecifyWindowLength=on  WindowLength=4  SimulateUsing=Code generation
  aux1 : Outport
  wires:
  Divide/1 -> aux1/1  "frac_dist"
  In1/1 -> Bus Selector/1
  Bus Selector/2 -> Divide/2  "<env_route_length>"
  Bus Selector/1 -> Moving Maximum/1  "<pos>"
  Moving Maximum/1 -> Divide/1

== system rs_bicycle/aux2: Fraction Spent In Forest ==
  In1 : Inport
  Bus Selector1 : BusSelector  OutputSignals=S.pos,P.forest_bounds
  Clock7 : Clock
  Constant : Constant  Value=0
  Divide : Product  Inputs=*/
  In Forest Boolearn : Subsystem
  Integrator : Integrator
  Switch : Switch  Criteria=u2 > Threshold
  aux2 : Outport
  wires:
  Integrator/1 -> Divide/1
  Bus Selector1/1 -> In Forest Boolearn/1("pos ")  "<pos>"
  In1/1 -> Bus Selector1/1
  Clock7/1 -> Switch/2, Divide/2
  In Forest Boolearn/1("in_forest ") -> Integrator/1  "in_forest"
  Bus Selector1/2 -> In Forest Boolearn/2(forest_bounds)  "<forest_bounds>"
  Divide/1 -> Switch/1  "frac_forest"
  Switch/1 -> aux2/1
  Constant/1 -> Switch/3

== system rs_bicycle/aux3: Closest Instantaenous Traffic ==
  In1 : Inport
  Abs : Abs
  Bus Selector3 : BusSelector  OutputSignals=S.pos,P.traffic_pos,P.traffic_passing
  Constant1 : Constant  Value=1/4 * env_route_length
  "Minimum Between Signals " : MATLAB Function  TreatAsAtomicUnit=on
  Sum : Sum  Inputs=|+-
  Switch2 : Switch  Criteria=u2 > Threshold
  aux1 : Outport
  wires:
  "Minimum Between Signals "/1(y) -> aux1/1
  Bus Selector3/3 -> Switch2/2  "<traffic_passing>"
  Switch2/1 -> "Minimum Between Signals "/1(u)
  Constant1/1 -> Switch2/3
  In1/1 -> Bus Selector3/1
  Sum/1 -> Abs/1
  Bus Selector3/1 -> Sum/1  "<pos>"
  Bus Selector3/2 -> Sum/2  "<traffic_pos>"
  Abs/1 -> Switch2/1

== system rs_bicycle/aux4: Instantaneous Stopping Distance ==
  In1 : Inport
  Bus Selector : BusSelector  OutputSignals=S.vel,P.static_friction
  Divide : Product  Inputs=*/
  Gain : Gain  Gain=2
  Product : Product
  Product1 : Product
  Square : Math  Operator=square  SignedPower=off  SaturateOnIntegerOverflow=on
  Sum : Sum  Inputs=|++
  gravity : Constant  Value=g
  reaction_time : Constant  Value=0.5
  aux4 : Outport
  wires:
  Bus Selector/2 -> Product1/1  "<static_friction>"
  Sum/1 -> aux4/1  "stopping_dist"
  Product/1 -> Sum/1
  Divide/1 -> Sum/2
  Square/1 -> Divide/1
  In1/1 -> Bus Selector/1
  Bus Selector/1 -> Product/1, Square/1  "<vel>"
  gravity/1 -> Product1/2
  Gain/1 -> Divide/2
  Product1/1 -> Gain/1
  reaction_time/1 -> Product/2

== system rs_bicycle/aux5: Cyclist Power Density Transfer ==
  In1 : Inport
  Bus Selector : BusSelector  OutputSignals=S.acc,S.vel
  Constant{,1..4} (5 alike) : Constant  Value=0
  Logical Operator : Logic  AllPortsSameDT=off  OutDataTypeStr=boolean
  Logical Operator1 : Logic  AllPortsSameDT=off  OutDataTypeStr=boolean
  Logical Operator2 : Logic  Operator=OR  AllPortsSameDT=off  OutDataTypeStr=boolean
  Product1 : Product
  Relational Operator : RelationalOperator  OutDataTypeStr=boolean  RndMeth=Simplest
  Relational Operator1 : RelationalOperator  OutDataTypeStr=boolean  RndMeth=Simplest
  Relational Operator2 : RelationalOperator  Operator=<  OutDataTypeStr=boolean  RndMeth=Simplest
  Relational Operator3 : RelationalOperator  Operator=<  OutDataTypeStr=boolean  RndMeth=Simplest
  Switch : Switch  Criteria=u2 > Threshold
  aux5 : Outport
  wires:
  Bus Selector/2 -> Relational Operator3/1, Relational Operator1/1, Product1/2  "<vel>"
  Product1/1 -> Switch/1  "cyclist_power_density"
  Bus Selector/1 -> Relational Operator2/1, Relational Operator/1, Product1/1  "<acc>"
  In1/1 -> Bus Selector/1
  Relational Operator/1 -> Logical Operator/1
  Relational Operator1/1 -> Logical Operator/2
  Constant/1 -> Relational Operator1/2
  Constant1/1 -> Relational Operator/2
  Constant2/1 -> Relational Operator3/2
  Relational Operator3/1 -> Logical Operator1/2
  Constant3/1 -> Relational Operator2/2
  Relational Operator2/1 -> Logical Operator1/1
  Logical Operator1/1 -> Logical Operator2/2
  Logical Operator/1 -> Logical Operator2/1
  Logical Operator2/1 -> Switch/2
  Switch/1 -> aux5/1
  Constant4/1 -> Switch/3

== system rs_bicycle/aux6: Exceedance of Static Friction (slipping) ==
  In1 : Inport
  Abs : Abs
  Bus Selector : BusSelector  OutputSignals=S.acc,P.static_friction
  Divide : Product  Inputs=*/
  Sum : Sum  Inputs=|+-
  gravity : Constant  Value=g
  aux6 : Outport
  wires:
  Bus Selector/1 -> Divide/1  "<acc>"
  Bus Selector/2 -> Sum/2  "<static_friction>"
  In1/1 -> Bus Selector/1
  Sum/1 -> aux6/1  "slipping"
  Divide/1 -> Abs/1
  gravity/1 -> Divide/2
  Abs/1 -> Sum/1

== system rs_bicycle/aux7: Final Velocity ==
  In1 : Inport
  Bus Selector : BusSelector  OutputSignals=S.vel
  aux7 : Outport
  wires:
  In1/1 -> Bus Selector/1
  Bus Selector/1 -> aux7/1  "<vel>"

== system rs_bicycle/aux8: Drag Power Compensation (V^3) ==
  In1 : Inport
  Abs : Abs
  Bus Selector : BusSelector  OutputSignals=S.vel
  Constant : Constant  Value=3
  Exp : Math  Operator=pow  SignedPower=off  SaturateOnIntegerOverflow=on
  aux8 : Outport
  wires:
  In1/1 -> Bus Selector/1
  Abs/1 -> aux8/1
  Exp/1 -> Abs/1
  Constant/1 -> Exp/2
  Bus Selector/1 -> Exp/1  "<vel>"

== system rs_bicycle/aux2: Fraction Spent In Forest/In Forest Boolearn ==
  "pos " : Inport
  forest_bounds : Inport  Port=2
  Constant : Constant
  Demux : Demux  Outputs=2
  Logical Operator : Logic  AllPortsSameDT=off  OutDataTypeStr=boolean
  Relational Operator : RelationalOperator  Operator=<=  OutDataTypeStr=boolean  RndMeth=Simplest
  Relational Operator1 : RelationalOperator  Operator=<=  OutDataTypeStr=boolean  RndMeth=Simplest
  Switch : Switch  Criteria=u2 > Threshold
  no : Constant  Value=0
  "in_forest " : Outport
  wires:
  Switch/1 -> "in_forest "/1
  Relational Operator/1 -> Logical Operator/1
  Relational Operator1/1 -> Logical Operator/2
  forest_bounds/1 -> Demux/1
  Logical Operator/1 -> Switch/2
  "pos "/1 -> Relational Operator/2, Relational Operator1/1
  Demux/1 -> Relational Operator/1
  Demux/2 -> Relational Operator1/2
  Constant/1 -> Switch/1
  no/1 -> Switch/3

== matlab function rs_bicycle/aux3: Closest Instantaenous Traffic/Minimum Between Signals  ==
function y = fcn(u)

y = min(u);
